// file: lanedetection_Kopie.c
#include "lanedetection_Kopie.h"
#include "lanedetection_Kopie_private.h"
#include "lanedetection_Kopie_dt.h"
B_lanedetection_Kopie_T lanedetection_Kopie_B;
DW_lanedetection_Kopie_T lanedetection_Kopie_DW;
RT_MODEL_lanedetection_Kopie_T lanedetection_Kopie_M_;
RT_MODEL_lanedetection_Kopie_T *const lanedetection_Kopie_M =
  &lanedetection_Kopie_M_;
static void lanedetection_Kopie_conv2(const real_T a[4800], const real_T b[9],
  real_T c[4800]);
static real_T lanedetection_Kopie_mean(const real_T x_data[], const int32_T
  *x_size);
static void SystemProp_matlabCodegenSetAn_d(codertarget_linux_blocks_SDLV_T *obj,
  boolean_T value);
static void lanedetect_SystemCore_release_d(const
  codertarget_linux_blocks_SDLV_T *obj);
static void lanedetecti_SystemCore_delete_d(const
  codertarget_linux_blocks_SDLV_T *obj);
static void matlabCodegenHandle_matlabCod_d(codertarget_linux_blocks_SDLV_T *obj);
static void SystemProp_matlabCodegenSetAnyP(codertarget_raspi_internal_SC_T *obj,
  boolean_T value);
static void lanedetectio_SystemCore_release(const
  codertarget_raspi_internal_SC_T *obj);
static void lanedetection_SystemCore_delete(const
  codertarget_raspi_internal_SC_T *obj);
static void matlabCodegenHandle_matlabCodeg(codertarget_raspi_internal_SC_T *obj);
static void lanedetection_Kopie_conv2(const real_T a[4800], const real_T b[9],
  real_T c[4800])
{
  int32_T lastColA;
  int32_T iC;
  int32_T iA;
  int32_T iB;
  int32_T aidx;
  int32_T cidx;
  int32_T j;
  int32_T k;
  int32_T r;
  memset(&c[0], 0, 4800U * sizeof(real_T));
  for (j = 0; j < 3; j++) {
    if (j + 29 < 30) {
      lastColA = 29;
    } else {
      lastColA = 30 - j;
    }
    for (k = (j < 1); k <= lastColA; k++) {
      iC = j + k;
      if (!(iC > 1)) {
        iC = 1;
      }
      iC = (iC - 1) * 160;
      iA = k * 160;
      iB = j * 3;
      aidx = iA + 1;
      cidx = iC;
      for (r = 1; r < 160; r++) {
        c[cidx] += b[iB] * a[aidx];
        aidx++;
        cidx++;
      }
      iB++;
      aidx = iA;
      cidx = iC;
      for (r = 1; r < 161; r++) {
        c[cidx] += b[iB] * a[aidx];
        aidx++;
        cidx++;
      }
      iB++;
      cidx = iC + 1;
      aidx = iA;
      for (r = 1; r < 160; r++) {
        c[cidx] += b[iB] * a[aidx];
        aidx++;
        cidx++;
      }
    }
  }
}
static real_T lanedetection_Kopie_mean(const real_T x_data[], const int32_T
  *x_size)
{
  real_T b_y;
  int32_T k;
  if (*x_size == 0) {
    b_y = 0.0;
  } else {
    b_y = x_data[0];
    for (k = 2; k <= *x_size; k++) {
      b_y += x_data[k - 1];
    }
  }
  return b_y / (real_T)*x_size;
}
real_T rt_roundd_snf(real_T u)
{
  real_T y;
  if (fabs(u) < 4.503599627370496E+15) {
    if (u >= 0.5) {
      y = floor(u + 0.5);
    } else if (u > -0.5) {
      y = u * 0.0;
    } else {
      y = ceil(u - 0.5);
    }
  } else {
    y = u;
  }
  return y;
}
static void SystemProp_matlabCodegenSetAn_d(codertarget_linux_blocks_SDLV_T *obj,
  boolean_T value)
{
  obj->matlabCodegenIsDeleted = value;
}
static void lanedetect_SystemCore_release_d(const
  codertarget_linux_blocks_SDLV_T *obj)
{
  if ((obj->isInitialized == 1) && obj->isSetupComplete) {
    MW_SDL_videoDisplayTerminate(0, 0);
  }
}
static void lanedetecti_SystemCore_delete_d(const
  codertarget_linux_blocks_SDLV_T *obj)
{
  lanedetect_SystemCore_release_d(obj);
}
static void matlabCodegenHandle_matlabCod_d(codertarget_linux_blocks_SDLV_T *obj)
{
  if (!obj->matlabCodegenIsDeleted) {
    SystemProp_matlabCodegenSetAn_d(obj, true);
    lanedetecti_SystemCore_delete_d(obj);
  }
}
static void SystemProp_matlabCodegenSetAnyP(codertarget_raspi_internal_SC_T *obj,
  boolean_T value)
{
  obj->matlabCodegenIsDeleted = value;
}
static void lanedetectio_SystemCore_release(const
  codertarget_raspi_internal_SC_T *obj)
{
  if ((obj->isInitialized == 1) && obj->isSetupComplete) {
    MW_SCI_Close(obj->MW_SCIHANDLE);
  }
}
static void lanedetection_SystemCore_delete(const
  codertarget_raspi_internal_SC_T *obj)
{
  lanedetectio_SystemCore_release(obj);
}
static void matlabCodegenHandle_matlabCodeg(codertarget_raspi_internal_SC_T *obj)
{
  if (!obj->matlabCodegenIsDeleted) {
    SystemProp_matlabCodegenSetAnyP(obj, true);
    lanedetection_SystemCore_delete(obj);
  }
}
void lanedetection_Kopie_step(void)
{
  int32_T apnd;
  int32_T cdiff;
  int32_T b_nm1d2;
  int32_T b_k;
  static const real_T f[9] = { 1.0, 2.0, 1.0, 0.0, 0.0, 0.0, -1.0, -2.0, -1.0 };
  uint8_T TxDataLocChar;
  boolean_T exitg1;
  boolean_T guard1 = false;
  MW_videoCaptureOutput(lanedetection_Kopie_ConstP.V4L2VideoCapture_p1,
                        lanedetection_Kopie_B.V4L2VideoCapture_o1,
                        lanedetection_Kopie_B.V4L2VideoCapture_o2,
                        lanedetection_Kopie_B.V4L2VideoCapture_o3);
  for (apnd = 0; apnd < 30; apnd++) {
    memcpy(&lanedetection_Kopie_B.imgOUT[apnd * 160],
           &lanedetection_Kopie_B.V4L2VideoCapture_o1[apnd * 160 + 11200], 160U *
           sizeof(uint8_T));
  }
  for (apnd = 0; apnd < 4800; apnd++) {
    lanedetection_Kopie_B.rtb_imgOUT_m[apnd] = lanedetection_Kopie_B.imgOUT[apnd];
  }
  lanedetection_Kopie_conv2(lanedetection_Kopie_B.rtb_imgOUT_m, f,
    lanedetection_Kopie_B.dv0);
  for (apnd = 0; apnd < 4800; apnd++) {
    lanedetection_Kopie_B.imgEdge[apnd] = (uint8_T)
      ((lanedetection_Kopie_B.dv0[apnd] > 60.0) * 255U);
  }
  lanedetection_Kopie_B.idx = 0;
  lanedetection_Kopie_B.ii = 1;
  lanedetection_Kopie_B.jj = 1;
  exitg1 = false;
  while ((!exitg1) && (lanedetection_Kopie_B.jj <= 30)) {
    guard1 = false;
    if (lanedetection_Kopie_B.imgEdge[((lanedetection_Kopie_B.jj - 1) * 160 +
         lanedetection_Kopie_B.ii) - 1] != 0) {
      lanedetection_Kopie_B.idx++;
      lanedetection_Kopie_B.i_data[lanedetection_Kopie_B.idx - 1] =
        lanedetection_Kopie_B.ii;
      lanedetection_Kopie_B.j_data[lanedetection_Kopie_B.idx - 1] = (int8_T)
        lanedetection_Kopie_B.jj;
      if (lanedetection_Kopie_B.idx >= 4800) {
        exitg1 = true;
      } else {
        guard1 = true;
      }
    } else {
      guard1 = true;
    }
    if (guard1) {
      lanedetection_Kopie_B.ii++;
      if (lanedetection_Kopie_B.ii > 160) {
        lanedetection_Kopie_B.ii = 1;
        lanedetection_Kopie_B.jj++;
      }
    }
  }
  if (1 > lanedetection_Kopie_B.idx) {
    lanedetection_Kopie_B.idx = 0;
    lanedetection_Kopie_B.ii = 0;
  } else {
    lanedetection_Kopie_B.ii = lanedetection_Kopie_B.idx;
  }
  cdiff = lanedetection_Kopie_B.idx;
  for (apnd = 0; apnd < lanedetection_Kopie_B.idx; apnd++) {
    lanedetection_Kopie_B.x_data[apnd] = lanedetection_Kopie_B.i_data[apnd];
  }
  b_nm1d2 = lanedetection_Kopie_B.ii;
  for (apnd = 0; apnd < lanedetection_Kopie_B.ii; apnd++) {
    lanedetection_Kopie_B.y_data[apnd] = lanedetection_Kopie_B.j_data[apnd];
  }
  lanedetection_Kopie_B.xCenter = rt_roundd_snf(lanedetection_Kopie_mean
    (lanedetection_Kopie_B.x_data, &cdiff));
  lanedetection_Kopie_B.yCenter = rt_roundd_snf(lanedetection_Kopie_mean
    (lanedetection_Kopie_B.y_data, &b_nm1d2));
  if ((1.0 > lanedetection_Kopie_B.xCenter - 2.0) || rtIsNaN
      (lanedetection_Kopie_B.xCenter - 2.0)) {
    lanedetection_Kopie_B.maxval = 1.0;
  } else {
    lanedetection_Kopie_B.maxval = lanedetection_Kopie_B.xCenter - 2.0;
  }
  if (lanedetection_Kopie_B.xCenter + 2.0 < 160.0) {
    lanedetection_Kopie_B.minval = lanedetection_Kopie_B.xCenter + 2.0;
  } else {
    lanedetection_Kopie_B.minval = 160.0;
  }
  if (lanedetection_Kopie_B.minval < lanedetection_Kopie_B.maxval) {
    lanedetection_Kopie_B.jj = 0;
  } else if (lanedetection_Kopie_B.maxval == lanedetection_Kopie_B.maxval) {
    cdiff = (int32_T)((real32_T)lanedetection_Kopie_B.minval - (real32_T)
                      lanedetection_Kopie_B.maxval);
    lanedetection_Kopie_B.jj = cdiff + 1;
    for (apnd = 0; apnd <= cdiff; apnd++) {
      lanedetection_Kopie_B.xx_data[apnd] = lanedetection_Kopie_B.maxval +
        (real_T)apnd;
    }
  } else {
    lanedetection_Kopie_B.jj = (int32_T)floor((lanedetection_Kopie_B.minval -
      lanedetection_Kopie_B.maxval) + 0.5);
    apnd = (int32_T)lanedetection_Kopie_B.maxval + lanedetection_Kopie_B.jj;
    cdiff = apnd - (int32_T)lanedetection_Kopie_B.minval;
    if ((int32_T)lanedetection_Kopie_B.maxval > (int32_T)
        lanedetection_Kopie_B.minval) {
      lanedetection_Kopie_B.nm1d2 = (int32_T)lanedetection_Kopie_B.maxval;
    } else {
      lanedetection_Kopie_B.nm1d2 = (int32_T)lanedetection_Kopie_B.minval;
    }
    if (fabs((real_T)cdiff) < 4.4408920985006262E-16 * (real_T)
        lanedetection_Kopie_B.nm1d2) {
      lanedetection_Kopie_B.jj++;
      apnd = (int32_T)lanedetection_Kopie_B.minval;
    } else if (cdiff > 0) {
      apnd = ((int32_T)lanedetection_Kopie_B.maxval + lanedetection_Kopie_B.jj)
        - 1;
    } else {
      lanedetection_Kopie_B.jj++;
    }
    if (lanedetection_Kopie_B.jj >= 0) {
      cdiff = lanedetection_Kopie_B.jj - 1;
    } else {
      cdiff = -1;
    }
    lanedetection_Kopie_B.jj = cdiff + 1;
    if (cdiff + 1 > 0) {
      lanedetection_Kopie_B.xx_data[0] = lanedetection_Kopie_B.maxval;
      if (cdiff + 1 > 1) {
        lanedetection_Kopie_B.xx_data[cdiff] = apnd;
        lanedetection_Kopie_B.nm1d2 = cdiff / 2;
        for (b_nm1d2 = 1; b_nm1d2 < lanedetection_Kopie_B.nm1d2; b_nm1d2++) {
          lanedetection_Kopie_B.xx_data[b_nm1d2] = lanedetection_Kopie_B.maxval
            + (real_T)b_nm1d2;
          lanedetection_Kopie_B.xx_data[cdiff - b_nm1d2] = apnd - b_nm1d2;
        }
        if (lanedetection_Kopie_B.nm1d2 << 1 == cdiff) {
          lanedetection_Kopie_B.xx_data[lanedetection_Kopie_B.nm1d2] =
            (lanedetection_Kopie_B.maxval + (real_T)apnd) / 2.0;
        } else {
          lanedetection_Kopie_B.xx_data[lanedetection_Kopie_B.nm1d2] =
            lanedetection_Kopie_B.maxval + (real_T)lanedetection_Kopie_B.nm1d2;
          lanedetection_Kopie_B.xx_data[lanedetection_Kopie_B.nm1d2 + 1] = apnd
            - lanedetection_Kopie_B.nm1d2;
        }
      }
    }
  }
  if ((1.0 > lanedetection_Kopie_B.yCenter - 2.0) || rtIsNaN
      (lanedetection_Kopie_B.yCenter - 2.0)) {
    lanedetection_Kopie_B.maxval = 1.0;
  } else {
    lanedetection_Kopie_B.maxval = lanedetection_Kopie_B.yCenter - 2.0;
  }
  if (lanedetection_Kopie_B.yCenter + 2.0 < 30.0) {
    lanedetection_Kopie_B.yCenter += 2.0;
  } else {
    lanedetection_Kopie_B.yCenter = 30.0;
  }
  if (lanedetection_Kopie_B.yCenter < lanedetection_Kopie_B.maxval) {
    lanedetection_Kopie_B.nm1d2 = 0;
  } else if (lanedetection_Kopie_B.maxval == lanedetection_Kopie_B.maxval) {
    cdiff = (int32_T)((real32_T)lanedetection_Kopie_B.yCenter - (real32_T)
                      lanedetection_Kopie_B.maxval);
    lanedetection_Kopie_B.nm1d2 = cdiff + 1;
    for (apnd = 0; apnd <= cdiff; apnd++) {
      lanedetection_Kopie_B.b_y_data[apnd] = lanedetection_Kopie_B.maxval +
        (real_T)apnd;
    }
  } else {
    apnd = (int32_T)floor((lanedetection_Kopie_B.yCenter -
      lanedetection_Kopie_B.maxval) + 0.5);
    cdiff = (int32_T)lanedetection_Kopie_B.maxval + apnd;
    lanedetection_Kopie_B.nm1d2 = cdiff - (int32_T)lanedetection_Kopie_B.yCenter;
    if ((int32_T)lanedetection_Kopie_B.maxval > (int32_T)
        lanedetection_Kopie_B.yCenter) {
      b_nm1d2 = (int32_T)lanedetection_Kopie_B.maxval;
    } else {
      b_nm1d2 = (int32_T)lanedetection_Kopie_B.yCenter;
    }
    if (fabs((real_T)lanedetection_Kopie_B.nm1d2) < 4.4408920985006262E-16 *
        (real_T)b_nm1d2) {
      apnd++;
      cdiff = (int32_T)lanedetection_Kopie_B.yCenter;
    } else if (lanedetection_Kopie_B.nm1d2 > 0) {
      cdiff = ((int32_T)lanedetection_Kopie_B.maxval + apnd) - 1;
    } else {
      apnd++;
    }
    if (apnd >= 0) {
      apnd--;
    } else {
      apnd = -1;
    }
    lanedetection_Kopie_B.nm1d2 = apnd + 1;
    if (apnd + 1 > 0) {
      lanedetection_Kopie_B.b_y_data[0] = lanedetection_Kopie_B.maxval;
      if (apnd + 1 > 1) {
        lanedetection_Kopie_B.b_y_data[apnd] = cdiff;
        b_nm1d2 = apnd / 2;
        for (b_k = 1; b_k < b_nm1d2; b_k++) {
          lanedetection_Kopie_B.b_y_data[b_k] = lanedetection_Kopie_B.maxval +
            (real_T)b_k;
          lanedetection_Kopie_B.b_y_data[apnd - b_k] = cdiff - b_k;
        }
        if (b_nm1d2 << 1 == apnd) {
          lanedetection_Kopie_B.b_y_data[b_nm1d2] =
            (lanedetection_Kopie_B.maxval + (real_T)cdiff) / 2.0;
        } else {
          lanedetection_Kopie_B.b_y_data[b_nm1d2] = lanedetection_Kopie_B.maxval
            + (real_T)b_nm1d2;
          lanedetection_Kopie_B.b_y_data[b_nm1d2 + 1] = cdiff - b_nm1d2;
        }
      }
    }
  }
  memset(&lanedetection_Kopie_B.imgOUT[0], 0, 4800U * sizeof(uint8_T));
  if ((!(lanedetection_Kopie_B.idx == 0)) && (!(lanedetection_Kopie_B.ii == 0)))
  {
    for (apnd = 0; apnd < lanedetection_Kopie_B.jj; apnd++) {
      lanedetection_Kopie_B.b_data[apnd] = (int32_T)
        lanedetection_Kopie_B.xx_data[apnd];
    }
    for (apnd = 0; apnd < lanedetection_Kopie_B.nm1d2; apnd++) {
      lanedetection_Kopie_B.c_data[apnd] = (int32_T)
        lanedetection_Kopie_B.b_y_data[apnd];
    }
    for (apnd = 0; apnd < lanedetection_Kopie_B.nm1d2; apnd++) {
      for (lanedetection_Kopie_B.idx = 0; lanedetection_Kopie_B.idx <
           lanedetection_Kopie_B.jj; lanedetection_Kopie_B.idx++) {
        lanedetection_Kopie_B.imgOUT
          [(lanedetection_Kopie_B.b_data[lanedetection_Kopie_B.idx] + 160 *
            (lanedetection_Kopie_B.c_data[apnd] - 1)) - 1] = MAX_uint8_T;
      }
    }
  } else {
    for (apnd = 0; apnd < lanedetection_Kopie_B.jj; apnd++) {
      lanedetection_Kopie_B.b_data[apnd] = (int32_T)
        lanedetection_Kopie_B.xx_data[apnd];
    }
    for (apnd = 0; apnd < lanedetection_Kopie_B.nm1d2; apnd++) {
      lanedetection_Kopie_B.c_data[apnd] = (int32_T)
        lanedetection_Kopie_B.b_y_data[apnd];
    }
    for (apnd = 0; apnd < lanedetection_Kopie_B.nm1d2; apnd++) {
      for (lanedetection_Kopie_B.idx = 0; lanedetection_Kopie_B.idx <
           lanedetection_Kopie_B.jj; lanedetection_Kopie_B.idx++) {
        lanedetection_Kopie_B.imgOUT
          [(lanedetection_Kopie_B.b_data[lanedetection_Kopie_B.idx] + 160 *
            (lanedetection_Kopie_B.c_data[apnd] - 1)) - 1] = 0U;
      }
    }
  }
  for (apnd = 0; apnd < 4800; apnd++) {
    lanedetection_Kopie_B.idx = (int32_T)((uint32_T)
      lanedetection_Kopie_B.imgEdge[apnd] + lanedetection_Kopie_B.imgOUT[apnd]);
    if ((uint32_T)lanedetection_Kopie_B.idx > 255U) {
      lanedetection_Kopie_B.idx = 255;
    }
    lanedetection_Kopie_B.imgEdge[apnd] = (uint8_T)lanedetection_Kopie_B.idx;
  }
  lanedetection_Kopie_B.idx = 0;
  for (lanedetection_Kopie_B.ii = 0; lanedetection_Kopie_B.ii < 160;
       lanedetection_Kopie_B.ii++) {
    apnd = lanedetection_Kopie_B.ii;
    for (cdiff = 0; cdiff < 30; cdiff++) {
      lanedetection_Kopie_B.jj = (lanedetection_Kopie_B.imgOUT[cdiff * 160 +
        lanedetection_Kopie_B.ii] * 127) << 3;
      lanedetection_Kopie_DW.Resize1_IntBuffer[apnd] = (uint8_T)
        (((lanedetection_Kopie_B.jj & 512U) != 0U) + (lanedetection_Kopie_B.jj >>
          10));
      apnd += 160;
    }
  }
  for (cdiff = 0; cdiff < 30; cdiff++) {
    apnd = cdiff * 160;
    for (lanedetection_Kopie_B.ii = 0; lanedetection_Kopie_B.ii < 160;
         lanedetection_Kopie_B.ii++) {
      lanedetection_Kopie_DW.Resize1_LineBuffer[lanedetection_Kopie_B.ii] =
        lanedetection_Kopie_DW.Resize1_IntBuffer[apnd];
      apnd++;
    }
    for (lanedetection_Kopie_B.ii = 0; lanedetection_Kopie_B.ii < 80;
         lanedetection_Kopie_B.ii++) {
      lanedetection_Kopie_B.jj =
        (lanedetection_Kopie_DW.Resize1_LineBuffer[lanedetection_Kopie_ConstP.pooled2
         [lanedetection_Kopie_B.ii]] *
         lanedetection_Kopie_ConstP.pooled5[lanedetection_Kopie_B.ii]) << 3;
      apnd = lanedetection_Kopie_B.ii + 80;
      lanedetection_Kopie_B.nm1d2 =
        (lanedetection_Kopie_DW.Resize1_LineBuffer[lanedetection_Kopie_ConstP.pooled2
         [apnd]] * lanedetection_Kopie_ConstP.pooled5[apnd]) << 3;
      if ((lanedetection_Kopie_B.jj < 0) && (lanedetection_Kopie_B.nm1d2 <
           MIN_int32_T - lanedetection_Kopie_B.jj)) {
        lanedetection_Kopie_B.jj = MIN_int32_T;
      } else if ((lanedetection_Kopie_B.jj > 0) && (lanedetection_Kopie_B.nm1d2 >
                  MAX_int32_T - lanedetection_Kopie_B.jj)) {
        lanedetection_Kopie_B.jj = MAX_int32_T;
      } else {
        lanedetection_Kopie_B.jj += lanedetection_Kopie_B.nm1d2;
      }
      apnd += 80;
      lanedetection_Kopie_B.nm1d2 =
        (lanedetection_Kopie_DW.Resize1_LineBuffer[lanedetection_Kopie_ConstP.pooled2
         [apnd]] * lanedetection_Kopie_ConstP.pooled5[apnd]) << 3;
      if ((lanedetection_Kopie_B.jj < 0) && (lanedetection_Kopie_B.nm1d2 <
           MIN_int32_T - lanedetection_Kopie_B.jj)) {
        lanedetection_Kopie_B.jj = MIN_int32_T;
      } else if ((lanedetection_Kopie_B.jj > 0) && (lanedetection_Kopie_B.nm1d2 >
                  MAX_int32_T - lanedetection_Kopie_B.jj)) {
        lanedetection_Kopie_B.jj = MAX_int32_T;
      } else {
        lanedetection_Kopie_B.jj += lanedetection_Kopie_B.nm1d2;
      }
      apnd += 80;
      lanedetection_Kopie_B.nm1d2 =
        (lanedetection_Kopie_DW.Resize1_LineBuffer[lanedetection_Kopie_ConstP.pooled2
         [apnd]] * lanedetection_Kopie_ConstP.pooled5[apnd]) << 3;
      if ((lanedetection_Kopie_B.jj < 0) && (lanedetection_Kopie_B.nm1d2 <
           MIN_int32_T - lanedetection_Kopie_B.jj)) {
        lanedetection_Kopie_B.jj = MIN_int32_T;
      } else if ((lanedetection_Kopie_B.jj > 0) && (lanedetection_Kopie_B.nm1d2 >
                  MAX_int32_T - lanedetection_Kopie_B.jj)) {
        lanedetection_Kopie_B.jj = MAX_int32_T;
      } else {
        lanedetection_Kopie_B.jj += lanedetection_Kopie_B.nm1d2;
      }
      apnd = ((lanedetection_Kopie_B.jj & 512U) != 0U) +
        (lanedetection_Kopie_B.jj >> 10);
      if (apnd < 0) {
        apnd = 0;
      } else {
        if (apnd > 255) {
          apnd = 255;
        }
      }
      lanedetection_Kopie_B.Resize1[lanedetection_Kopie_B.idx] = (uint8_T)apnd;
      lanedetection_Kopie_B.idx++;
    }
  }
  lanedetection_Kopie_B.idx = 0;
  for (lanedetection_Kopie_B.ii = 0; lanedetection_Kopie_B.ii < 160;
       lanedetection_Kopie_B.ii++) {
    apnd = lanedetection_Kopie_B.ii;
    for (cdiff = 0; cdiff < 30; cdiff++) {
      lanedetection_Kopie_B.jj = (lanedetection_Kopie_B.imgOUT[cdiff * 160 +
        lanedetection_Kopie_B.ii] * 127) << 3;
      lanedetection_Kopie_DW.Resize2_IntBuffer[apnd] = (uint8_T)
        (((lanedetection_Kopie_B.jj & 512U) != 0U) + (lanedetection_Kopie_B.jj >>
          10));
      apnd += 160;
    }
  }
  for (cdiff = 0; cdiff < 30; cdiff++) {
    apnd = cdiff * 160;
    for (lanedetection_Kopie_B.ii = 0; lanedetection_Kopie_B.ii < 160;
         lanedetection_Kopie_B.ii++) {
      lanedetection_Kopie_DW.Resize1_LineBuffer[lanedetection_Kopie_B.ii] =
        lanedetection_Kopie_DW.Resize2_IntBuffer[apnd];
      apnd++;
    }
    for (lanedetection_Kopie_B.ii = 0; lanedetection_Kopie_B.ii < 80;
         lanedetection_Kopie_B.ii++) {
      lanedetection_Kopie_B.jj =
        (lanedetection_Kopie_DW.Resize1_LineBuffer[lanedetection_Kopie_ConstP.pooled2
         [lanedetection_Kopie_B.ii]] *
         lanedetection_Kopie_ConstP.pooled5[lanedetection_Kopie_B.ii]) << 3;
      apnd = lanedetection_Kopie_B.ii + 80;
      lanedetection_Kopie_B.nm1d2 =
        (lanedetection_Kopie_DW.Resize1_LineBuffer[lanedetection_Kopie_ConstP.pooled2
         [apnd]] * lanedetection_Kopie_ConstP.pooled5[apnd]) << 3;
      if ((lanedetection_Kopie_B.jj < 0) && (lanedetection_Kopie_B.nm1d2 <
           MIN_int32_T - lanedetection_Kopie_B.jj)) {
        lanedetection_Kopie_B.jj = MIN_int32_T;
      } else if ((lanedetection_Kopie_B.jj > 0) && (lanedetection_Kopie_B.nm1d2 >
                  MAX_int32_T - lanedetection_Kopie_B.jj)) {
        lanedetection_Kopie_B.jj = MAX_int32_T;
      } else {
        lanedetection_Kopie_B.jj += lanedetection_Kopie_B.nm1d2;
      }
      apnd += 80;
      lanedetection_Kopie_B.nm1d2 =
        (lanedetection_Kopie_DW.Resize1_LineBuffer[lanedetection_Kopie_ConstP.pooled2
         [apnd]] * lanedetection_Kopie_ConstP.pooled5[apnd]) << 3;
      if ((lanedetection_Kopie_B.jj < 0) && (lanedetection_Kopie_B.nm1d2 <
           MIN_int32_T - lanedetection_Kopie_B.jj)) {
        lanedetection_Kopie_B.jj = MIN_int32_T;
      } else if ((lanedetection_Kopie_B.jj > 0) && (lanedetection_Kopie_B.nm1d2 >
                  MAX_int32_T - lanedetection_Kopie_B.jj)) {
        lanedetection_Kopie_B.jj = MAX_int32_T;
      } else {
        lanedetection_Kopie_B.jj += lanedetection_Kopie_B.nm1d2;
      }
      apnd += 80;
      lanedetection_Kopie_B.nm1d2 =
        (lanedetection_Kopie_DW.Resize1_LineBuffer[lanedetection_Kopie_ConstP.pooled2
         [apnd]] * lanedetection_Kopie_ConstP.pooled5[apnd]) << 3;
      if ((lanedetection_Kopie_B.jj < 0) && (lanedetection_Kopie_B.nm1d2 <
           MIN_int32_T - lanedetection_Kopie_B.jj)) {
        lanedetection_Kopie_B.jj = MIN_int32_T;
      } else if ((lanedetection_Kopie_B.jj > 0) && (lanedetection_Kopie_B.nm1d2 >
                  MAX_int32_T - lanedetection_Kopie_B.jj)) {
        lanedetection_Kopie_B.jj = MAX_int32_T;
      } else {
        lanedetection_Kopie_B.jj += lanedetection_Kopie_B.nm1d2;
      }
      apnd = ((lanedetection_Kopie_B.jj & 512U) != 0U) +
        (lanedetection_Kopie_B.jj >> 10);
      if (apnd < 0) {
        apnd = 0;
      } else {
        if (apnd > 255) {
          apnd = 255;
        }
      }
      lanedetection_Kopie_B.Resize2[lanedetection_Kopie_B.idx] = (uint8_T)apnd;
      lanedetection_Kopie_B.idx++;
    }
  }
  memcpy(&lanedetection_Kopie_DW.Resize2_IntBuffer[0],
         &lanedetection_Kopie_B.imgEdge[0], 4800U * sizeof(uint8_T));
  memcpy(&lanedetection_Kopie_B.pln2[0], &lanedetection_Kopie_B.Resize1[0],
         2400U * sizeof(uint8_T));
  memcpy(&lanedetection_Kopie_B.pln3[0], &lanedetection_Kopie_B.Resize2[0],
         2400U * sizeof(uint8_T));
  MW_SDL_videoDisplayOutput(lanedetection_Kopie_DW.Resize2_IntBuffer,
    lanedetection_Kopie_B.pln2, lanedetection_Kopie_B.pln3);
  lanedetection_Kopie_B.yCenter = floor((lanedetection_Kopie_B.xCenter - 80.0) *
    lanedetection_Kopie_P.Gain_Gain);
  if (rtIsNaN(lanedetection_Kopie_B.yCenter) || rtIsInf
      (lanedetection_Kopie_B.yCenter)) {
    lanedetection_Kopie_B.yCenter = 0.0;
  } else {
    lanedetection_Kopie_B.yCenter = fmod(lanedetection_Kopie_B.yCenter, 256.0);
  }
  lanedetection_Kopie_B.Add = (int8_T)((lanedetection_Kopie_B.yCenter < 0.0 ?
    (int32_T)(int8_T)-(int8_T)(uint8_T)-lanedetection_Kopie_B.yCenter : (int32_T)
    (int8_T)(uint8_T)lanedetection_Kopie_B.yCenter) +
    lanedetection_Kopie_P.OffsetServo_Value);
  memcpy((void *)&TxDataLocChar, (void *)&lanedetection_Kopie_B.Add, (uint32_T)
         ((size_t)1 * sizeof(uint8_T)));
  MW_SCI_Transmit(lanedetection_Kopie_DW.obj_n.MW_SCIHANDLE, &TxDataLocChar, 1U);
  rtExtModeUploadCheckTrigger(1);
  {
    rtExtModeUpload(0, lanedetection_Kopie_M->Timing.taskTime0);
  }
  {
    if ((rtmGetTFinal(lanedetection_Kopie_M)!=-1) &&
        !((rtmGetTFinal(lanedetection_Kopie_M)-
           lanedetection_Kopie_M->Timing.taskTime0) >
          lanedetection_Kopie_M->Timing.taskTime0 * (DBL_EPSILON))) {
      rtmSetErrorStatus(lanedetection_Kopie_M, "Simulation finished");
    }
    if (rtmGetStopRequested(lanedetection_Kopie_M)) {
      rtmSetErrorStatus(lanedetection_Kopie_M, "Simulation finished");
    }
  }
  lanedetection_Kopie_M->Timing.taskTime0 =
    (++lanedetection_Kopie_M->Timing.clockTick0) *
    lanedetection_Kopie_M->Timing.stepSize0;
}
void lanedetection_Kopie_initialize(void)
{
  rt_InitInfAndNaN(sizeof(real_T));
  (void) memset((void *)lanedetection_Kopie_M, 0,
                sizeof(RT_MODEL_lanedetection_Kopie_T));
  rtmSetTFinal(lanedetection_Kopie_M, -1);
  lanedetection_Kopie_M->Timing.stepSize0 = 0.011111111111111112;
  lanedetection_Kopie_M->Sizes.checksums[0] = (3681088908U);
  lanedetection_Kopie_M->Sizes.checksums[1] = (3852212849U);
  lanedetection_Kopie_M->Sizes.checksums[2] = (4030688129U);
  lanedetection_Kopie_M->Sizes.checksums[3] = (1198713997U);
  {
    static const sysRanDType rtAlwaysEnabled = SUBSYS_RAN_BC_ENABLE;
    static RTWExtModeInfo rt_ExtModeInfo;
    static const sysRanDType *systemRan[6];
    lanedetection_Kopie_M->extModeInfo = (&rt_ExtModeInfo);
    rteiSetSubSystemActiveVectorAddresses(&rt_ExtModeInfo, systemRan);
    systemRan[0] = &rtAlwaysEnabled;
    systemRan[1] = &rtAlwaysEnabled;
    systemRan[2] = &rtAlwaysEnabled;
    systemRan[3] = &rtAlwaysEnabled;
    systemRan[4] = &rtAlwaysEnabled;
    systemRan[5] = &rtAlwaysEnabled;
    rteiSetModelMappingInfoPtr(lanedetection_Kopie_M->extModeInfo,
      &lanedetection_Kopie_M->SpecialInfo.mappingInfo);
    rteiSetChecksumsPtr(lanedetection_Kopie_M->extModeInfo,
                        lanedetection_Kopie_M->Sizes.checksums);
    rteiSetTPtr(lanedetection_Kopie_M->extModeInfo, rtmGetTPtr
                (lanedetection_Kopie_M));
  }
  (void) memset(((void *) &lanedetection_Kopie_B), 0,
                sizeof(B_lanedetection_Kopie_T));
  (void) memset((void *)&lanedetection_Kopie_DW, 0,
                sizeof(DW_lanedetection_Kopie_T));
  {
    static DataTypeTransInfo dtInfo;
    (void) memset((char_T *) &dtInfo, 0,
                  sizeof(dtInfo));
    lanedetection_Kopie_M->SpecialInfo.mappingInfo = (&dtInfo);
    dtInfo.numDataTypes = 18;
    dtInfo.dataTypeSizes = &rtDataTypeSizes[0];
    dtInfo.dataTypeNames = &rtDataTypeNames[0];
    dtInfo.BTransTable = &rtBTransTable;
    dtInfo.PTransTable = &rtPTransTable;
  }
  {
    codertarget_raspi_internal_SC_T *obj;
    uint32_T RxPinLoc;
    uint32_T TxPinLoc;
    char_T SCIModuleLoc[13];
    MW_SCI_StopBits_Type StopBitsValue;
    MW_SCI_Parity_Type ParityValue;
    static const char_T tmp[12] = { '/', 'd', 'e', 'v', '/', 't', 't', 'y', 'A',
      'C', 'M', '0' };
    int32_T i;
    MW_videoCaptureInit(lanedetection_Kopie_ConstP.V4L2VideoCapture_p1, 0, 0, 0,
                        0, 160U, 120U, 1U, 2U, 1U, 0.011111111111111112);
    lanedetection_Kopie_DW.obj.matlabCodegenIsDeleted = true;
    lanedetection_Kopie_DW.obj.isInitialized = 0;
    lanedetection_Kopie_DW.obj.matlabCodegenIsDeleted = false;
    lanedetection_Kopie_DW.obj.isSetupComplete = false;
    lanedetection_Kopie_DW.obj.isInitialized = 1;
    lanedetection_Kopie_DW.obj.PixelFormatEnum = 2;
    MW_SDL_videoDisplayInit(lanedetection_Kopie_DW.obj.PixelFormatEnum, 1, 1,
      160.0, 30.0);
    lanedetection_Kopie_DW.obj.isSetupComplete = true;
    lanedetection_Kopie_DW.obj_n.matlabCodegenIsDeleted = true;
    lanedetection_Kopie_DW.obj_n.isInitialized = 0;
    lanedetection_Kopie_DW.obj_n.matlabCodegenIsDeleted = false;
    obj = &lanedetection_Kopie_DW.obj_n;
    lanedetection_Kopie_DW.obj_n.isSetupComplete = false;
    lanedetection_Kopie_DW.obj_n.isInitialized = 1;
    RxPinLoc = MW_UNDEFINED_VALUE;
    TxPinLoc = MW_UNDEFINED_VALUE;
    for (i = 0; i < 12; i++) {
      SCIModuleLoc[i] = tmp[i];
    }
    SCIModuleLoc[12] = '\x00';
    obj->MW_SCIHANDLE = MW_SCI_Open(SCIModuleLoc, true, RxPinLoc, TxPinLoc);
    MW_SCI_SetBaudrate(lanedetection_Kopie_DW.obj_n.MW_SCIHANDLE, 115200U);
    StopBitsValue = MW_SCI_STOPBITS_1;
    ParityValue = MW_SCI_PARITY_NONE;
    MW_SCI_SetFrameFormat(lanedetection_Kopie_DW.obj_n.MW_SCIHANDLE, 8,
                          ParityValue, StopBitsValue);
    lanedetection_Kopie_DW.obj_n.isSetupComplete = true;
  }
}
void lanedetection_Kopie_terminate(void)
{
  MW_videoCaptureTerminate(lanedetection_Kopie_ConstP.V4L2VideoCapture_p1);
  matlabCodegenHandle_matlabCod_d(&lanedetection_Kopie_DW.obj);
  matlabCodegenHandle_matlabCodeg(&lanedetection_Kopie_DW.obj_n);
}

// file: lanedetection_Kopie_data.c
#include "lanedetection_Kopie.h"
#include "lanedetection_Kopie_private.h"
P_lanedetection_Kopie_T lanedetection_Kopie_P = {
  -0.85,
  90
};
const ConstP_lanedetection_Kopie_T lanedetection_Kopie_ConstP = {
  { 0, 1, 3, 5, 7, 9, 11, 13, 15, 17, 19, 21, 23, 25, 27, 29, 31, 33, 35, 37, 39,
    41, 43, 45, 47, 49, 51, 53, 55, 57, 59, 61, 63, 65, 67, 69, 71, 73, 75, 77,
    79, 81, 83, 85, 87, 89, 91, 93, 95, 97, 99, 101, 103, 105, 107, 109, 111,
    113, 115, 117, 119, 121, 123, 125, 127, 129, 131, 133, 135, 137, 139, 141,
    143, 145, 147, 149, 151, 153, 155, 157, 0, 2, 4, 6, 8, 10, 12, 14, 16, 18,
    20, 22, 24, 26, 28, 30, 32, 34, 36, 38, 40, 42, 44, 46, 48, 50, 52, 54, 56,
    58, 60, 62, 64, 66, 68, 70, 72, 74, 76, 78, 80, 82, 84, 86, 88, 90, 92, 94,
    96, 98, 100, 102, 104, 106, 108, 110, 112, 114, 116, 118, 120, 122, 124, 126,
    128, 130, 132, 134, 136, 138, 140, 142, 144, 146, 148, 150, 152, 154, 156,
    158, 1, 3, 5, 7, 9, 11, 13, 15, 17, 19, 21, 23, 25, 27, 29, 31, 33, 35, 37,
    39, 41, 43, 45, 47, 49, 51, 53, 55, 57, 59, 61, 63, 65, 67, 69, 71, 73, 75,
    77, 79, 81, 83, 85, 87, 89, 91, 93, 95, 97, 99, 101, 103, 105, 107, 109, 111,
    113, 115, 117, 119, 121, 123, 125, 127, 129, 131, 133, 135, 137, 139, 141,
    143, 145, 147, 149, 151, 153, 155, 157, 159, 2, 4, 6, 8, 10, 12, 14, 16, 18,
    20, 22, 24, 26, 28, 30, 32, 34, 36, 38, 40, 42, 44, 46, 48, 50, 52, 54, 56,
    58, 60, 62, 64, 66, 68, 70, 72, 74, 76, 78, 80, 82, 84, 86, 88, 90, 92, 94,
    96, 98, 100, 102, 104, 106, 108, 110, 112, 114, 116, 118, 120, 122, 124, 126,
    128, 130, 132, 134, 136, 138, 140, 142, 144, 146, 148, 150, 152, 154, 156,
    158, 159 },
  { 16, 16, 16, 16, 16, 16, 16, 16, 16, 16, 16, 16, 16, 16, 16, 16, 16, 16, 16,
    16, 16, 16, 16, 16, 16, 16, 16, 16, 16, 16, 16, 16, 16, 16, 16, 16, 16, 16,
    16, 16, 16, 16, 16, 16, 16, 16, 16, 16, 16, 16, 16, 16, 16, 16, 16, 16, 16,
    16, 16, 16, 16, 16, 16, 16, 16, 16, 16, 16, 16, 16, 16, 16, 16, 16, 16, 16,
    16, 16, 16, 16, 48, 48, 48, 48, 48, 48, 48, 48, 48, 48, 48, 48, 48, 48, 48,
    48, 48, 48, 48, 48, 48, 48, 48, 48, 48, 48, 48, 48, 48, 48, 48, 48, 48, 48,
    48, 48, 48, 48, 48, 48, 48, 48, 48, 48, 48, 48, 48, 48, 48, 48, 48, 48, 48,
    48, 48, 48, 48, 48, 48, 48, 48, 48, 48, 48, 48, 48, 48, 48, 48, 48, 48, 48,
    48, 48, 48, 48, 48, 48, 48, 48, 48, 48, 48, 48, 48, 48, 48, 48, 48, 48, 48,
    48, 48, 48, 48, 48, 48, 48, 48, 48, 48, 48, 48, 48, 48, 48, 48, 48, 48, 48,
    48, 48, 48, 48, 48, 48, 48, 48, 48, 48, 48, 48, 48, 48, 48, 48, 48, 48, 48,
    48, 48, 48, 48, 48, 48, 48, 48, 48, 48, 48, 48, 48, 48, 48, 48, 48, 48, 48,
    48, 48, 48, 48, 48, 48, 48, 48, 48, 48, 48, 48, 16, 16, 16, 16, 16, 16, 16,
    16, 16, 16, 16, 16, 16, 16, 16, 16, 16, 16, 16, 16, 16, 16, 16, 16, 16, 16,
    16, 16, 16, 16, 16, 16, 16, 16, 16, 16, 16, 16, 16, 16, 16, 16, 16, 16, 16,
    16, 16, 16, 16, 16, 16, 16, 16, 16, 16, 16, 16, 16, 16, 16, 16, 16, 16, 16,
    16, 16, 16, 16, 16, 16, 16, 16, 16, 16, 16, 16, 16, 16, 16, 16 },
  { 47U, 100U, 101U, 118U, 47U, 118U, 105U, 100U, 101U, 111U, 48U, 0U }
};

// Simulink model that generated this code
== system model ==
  SerialWrite#1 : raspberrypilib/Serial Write  <- 1: Add
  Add : Sum  <- 1: DataTypeConversion#1, 2: OffsetServo
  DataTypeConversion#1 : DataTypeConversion  <- 1: Gain
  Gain : Gain  Gain=-0.85  <- 1: MATLABFunction#1/4
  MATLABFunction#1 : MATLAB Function  <- 1: MATLABFunction#2
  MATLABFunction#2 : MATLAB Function  <- 1: V4L2VideoCapture
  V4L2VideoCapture : embdlinuxlib/V4L2 Video Capture
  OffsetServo : Constant  Value=90
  SDLVideoDisplay#1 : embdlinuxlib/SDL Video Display  <- 1: MATLABFunction#1, 2: Resize1, 3: Resize2
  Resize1 : visiongeotforms/Resize  <- 1: MATLABFunction#1/2
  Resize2 : visiongeotforms/Resize  <- 1: MATLABFunction#1/3
== matlab function MATLABFunction#2 ==
function imgOUT   = imgROI(imgIN)

    % imgIN Array von 160x120
    % rectangle('Position',[x,y,w,h])
    
    imgOUT = imgIN(1:160,71:100);

end

== matlab function MATLABFunction#1 ==
function [imgEdge, CbDot, CrDot, centerOffset, xCenter]  = lanedetection(imgCam)

    threshold = 60;

    % create laplacian filter
    k = [1 2 1; 0 0 0; -1 -2 -1];
    % run sobel
    V = conv2(double(imgCam), k', 'same');
    % filter edges
    imgEdges = uint8((V > threshold) * 255);
    
    % Ab hier für Spurberechnung irrelevant
    
    
    
    % coordinates of all detected objects
    [x, y] = find(imgEdges);
    
    % detect the center of all objects
    xCenter = round(mean(x));
    yCenter = round(mean(y));
    
    % create vector xx and yy for an area around the center of all objects
    xx = max(1, xCenter-2):min(xCenter+2, size(imgEdges, 1));
    yy = max(1, yCenter-2):min(yCenter+2, size(imgEdges, 2));
    
    % create new array with the size of "bw" and fill it with "0"
    bwdot = zeros(size(imgEdges), 'uint8');
    
    % if there is something detected at x and y...
    if ~isempty(x) && ~isempty(y)
        % ...mark the area around the center
        bwdot(xx, yy) = 255;
    % if nothing gets detected...
    else
        bwdot(xx, yy) = 0;
    end
    
    % add the marked area around the center to the array justRed
    imgEdge = imgEdges + bwdot;
    CbDot = bwdot;
    CrDot = bwdot;
    centerOffset = (xCenter - 80);
end
